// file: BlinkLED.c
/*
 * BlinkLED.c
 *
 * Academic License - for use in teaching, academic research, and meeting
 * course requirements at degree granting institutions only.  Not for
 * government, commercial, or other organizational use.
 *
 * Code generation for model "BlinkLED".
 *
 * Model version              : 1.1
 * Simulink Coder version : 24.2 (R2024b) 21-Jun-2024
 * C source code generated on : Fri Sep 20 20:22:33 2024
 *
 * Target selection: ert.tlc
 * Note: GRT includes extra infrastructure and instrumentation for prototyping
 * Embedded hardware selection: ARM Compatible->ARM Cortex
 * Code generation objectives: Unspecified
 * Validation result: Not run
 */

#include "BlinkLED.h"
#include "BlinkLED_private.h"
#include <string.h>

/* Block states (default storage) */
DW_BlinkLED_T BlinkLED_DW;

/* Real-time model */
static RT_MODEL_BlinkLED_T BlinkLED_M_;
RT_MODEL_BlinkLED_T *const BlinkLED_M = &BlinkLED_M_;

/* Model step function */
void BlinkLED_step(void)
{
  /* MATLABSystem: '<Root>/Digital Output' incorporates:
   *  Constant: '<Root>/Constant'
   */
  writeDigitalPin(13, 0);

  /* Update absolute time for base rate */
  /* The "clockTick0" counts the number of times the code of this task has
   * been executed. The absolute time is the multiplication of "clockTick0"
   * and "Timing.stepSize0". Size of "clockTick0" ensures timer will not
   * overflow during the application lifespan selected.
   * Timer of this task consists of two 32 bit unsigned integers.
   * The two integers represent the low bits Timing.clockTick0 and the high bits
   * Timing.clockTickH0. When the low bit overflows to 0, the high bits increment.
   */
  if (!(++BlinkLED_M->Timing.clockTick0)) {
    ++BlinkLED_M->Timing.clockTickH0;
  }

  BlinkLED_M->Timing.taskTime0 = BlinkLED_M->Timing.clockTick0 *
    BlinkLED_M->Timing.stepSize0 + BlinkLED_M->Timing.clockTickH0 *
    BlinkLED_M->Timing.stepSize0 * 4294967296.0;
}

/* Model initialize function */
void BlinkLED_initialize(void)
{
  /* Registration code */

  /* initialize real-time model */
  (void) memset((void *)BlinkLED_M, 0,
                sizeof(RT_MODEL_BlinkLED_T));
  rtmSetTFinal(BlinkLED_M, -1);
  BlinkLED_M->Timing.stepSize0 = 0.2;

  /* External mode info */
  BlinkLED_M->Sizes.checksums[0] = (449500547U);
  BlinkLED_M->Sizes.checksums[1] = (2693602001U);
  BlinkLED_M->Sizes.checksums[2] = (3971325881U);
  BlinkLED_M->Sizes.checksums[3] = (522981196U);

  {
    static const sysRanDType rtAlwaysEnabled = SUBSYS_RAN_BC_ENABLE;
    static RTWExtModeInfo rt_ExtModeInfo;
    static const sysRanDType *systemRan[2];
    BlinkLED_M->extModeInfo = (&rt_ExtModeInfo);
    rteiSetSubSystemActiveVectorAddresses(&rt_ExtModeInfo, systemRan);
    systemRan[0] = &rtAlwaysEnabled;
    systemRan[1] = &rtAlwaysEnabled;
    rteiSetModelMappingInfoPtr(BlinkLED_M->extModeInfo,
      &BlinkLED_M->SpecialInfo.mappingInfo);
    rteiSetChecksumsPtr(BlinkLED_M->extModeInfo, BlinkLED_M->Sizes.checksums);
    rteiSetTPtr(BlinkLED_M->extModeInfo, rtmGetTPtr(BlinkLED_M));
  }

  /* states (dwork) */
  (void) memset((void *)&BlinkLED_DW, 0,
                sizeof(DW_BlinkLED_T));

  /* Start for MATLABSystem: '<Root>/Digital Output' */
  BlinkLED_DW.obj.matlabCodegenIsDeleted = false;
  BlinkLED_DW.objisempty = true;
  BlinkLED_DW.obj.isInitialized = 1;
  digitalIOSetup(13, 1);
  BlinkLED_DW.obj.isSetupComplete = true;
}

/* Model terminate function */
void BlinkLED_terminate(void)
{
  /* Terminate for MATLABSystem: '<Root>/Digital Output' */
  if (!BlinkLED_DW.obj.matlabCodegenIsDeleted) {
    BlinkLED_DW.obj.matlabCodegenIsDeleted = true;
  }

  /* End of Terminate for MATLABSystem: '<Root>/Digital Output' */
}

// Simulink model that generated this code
simulink model "BlinkLED"  (R2024b)
settings: Solver=FixedStepAuto  StartTime=0.0  StopTime=inf  RelTol=1e-3  EnableMultiTasking=on
libraries: arduinolib x1

== system BlinkLED ==
  Constant : Constant  Value=0
  Digital Output : arduinolib/Digital Output  pinNumber=13  Direction=output  blockPlatform=arduino
  wires:
  Constant/1 -> Digital Output/1
